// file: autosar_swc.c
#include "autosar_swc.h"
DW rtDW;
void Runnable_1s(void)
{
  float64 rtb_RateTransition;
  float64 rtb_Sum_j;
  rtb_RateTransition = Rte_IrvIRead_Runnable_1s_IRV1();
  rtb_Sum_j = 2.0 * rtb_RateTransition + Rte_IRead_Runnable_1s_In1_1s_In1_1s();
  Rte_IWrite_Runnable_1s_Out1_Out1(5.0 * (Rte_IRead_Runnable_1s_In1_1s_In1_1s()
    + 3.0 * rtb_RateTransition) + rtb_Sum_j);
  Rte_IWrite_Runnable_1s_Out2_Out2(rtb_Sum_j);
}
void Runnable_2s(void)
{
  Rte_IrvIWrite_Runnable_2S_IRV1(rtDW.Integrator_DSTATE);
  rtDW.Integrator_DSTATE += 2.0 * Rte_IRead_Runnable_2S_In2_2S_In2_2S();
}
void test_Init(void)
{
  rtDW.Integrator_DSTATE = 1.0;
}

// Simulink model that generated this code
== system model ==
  In1_1s : Inport
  In2_2S : Inport
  Out1 : Outport  <- 1: Sum
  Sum : Sum  Inputs=++  <- 1: Gain#1, 2: Sum#1
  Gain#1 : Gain  Gain=5  <- 1: Sum#2
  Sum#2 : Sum  Inputs=++  <- 1: In1_1s, 2: Gain#2
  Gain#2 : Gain  Gain=3  <- 1: RateTransition
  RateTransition : RateTransition  <- 1: Integrator
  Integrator : DiscreteIntegrator  <- 1: In2_2S
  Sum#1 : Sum  Inputs=++  <- 1: Gain#3, 2: In1_1s
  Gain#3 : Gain  Gain=2  <- 1: RateTransition
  Out2 : Outport  <- 1: Sum#1
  Subsystem#1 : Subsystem
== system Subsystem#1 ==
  StateWriter#1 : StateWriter  <- 1: Constant#1
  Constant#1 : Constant
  EventListener#1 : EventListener
